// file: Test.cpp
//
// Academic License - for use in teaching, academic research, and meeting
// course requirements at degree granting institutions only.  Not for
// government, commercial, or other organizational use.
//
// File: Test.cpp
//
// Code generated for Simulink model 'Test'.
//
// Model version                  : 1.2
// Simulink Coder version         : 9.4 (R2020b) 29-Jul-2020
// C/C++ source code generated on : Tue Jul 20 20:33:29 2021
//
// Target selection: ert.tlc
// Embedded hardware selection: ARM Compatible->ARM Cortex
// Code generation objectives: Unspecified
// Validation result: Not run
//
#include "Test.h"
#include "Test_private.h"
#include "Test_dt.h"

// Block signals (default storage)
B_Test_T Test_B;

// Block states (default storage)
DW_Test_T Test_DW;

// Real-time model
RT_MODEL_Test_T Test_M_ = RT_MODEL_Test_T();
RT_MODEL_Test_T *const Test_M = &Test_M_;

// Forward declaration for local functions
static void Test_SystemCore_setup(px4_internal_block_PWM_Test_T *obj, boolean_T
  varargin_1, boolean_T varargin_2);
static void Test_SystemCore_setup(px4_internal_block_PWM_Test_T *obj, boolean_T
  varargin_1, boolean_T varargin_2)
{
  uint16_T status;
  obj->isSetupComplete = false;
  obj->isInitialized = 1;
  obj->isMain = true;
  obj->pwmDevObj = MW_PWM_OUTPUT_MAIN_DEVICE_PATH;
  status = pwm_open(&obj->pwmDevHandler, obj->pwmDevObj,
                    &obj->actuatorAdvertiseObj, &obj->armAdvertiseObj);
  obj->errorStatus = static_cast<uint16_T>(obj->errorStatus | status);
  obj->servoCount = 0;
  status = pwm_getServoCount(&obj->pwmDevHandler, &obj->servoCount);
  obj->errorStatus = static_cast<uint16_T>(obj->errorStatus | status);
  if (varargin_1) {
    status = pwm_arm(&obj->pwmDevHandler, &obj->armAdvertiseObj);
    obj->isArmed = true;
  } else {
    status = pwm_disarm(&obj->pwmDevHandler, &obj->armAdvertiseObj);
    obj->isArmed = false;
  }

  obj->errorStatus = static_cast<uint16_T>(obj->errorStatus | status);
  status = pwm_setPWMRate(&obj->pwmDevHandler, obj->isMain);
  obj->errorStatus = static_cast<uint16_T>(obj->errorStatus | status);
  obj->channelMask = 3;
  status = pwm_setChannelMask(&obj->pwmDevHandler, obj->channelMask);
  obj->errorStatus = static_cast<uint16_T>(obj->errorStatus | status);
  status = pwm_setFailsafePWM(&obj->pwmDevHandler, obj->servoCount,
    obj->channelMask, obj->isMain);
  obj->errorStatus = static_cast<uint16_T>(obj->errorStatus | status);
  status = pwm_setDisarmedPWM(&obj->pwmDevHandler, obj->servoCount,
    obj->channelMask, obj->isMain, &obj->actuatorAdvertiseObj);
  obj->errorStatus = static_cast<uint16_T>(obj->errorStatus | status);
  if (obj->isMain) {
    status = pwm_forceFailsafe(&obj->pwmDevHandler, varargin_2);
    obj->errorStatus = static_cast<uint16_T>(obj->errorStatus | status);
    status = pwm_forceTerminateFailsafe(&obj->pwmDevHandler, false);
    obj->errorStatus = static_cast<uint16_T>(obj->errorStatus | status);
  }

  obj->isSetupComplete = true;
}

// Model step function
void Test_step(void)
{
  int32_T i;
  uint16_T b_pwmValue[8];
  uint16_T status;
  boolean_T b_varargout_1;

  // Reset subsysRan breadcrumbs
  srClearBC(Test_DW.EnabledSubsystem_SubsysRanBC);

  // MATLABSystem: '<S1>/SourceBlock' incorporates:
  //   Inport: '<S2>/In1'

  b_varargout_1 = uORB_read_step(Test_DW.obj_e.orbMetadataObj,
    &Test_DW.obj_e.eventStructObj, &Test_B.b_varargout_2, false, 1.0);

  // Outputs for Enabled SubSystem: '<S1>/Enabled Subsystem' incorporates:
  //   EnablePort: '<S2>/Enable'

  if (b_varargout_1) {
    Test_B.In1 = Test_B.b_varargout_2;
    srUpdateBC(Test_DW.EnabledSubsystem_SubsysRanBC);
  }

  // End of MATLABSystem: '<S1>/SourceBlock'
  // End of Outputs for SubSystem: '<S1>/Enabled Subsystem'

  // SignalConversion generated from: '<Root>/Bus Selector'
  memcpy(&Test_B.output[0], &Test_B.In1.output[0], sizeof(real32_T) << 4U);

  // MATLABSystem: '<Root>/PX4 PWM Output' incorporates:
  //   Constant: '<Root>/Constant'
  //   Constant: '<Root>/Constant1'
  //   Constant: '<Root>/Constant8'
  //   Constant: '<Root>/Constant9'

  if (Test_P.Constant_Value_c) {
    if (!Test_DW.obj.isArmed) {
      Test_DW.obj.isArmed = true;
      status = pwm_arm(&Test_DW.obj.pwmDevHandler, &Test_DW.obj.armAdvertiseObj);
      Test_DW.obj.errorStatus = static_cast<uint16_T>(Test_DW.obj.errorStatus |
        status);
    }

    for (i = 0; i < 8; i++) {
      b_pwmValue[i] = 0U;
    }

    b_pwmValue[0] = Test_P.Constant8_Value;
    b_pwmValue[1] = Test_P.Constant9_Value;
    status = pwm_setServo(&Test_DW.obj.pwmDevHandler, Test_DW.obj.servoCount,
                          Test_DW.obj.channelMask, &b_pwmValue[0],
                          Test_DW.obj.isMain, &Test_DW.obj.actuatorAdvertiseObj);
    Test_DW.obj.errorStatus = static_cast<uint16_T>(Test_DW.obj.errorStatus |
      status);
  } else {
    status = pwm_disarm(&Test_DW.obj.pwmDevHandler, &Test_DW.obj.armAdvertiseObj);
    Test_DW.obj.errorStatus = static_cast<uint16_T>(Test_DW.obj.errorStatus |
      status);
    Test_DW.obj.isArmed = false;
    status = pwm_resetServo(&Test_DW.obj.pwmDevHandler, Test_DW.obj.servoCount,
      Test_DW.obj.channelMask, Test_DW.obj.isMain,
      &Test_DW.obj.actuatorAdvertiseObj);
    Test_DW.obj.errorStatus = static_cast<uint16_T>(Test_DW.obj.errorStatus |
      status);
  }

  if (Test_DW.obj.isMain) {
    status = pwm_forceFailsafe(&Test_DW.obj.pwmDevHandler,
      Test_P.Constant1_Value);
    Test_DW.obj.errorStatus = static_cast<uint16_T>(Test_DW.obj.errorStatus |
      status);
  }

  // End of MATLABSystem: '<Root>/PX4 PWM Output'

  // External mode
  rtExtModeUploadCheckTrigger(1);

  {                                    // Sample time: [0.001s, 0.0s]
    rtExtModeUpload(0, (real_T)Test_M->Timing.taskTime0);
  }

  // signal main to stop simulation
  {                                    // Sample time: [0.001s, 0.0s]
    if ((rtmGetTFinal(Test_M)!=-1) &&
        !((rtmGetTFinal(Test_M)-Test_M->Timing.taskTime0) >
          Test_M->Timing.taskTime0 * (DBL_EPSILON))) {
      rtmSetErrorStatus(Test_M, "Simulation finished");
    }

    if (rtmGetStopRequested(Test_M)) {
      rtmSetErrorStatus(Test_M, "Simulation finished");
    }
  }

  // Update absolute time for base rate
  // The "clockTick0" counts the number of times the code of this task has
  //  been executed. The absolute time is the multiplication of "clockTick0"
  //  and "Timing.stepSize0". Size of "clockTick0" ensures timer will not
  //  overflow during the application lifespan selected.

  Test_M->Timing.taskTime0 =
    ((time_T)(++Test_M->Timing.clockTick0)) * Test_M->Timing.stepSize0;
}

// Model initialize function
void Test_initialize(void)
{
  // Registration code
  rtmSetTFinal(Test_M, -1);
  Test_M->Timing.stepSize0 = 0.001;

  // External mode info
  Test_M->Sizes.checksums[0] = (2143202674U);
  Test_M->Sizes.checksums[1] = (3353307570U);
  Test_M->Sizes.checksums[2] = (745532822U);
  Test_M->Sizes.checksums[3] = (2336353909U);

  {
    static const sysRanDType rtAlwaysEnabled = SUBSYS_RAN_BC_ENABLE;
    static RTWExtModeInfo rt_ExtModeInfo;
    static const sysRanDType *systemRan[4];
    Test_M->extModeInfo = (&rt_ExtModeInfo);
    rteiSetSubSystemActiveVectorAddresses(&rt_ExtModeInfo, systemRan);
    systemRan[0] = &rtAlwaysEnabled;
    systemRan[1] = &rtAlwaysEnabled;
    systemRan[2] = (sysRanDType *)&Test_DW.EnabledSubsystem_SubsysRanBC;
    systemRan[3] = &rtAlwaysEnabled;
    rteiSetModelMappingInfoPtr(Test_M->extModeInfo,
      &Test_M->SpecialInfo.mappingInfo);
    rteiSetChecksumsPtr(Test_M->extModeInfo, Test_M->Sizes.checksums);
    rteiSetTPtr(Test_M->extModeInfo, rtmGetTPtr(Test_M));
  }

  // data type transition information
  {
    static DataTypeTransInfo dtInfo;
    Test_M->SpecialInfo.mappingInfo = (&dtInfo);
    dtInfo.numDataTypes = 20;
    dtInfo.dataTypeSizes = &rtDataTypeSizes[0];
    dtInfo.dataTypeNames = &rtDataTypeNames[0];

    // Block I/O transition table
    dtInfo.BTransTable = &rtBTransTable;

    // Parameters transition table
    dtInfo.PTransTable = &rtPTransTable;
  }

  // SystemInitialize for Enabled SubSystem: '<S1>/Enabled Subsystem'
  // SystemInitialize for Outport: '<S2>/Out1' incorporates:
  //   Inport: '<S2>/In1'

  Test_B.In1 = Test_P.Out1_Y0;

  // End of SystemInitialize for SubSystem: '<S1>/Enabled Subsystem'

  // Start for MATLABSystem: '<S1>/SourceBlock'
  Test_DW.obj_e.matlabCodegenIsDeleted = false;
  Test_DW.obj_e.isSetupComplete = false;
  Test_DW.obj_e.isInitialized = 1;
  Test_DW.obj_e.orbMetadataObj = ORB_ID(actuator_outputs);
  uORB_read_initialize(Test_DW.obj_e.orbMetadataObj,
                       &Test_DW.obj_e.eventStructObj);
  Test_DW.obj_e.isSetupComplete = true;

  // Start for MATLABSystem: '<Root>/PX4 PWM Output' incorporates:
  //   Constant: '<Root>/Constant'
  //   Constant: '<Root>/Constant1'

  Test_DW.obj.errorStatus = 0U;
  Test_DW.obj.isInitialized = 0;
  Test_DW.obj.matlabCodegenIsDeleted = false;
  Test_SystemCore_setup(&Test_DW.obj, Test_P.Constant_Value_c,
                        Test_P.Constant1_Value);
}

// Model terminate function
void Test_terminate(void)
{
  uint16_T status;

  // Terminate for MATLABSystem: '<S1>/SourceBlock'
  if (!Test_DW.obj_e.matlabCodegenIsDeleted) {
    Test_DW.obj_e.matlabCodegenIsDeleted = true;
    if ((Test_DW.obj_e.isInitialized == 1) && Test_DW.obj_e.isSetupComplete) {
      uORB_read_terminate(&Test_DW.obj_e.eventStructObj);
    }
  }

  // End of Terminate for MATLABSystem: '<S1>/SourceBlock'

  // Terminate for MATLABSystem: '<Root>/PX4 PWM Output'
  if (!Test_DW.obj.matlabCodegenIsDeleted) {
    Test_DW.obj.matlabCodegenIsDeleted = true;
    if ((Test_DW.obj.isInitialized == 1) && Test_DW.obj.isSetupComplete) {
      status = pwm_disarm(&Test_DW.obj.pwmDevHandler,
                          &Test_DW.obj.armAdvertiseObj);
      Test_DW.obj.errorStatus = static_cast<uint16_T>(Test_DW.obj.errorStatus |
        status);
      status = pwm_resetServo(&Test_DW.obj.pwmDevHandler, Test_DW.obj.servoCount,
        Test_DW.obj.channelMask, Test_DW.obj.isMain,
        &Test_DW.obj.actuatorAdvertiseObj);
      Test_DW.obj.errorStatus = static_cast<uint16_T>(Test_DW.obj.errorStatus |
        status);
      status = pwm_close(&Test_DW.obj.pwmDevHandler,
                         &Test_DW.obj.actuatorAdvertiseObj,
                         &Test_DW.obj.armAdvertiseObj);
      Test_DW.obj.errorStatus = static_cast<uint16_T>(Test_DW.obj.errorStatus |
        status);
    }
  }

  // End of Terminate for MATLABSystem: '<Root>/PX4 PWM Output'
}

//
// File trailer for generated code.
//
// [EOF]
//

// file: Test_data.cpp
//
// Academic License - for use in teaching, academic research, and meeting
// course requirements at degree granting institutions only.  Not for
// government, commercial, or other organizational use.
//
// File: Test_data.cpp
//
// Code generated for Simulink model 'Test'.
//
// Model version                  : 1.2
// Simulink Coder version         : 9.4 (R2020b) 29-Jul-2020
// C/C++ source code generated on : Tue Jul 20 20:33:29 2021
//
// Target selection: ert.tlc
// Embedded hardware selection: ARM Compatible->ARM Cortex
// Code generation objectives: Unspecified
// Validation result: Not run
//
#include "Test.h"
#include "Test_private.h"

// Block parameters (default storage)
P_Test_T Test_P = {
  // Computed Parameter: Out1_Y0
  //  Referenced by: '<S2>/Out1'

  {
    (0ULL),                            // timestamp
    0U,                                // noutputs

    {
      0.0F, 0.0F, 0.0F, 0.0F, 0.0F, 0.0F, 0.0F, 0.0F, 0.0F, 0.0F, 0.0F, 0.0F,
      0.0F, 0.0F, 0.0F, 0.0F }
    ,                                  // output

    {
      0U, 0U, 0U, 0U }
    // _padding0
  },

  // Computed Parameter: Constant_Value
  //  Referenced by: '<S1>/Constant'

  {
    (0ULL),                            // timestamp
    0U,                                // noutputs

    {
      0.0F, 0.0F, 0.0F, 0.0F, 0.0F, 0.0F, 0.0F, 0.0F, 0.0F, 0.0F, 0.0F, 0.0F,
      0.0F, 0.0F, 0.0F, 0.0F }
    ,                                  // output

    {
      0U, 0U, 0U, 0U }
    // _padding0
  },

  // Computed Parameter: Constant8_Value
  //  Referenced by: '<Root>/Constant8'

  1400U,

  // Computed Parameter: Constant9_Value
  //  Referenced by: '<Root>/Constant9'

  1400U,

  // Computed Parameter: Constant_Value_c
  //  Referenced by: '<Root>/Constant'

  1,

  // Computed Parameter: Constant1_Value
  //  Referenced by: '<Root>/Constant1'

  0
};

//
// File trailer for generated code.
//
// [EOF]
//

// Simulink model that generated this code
simulink model "Test"  (R2020b)
settings: Solver=FixedStepAuto  StartTime=0.0  StopTime=inf  RelTol=1e-3  EnableMultiTasking=on
undefined symbols (not defined in the file or in its folder): dev, Main, pwm_output0
libraries: px4lib x1, px4uORBlib x1

== system Test ==
  Bus Selector : BusSelector  OutputSignals=output
  Constant : Constant  OutDataTypeStr=boolean
  Constant1 : Constant  Value=0  OutDataTypeStr=boolean
  Constant8 : Constant  Value=1400  OutDataTypeStr=uint16
  Constant9 : Constant  Value=1400  OutDataTypeStr=uint16
  Display : Display
  PX4 PWM Output : px4lib/PX4 PWM Output  pwmDevice=Main (/dev/pwm_output0)  pwmChannel1_=on  pwmChannel2_=on  pwmChannel3_=off  pwmChannel4_=off  pwmChannel5_=off  pwmChannel6_=off  pwmChannel7_=off  pwmChannel8_=off  forceTerminateFailsafe=off  outputErrorStatus=off
  PX4 uORB Read : px4uORBlib/PX4 uORB Read  uORBTopic=actuator_outputs  selectInstance=actuator_outputs  SampleTime=0.001  BlockingMode=off  BlockTimeout=1e-3
  wires:
  Constant/1 -> PX4 PWM Output/1
  Constant1/1 -> PX4 PWM Output/2
  Constant9/1 -> PX4 PWM Output/4
  Constant8/1 -> PX4 PWM Output/3
  PX4 uORB Read/2 -> Bus Selector/1
  Bus Selector/1 -> Display/1  "<output>"
